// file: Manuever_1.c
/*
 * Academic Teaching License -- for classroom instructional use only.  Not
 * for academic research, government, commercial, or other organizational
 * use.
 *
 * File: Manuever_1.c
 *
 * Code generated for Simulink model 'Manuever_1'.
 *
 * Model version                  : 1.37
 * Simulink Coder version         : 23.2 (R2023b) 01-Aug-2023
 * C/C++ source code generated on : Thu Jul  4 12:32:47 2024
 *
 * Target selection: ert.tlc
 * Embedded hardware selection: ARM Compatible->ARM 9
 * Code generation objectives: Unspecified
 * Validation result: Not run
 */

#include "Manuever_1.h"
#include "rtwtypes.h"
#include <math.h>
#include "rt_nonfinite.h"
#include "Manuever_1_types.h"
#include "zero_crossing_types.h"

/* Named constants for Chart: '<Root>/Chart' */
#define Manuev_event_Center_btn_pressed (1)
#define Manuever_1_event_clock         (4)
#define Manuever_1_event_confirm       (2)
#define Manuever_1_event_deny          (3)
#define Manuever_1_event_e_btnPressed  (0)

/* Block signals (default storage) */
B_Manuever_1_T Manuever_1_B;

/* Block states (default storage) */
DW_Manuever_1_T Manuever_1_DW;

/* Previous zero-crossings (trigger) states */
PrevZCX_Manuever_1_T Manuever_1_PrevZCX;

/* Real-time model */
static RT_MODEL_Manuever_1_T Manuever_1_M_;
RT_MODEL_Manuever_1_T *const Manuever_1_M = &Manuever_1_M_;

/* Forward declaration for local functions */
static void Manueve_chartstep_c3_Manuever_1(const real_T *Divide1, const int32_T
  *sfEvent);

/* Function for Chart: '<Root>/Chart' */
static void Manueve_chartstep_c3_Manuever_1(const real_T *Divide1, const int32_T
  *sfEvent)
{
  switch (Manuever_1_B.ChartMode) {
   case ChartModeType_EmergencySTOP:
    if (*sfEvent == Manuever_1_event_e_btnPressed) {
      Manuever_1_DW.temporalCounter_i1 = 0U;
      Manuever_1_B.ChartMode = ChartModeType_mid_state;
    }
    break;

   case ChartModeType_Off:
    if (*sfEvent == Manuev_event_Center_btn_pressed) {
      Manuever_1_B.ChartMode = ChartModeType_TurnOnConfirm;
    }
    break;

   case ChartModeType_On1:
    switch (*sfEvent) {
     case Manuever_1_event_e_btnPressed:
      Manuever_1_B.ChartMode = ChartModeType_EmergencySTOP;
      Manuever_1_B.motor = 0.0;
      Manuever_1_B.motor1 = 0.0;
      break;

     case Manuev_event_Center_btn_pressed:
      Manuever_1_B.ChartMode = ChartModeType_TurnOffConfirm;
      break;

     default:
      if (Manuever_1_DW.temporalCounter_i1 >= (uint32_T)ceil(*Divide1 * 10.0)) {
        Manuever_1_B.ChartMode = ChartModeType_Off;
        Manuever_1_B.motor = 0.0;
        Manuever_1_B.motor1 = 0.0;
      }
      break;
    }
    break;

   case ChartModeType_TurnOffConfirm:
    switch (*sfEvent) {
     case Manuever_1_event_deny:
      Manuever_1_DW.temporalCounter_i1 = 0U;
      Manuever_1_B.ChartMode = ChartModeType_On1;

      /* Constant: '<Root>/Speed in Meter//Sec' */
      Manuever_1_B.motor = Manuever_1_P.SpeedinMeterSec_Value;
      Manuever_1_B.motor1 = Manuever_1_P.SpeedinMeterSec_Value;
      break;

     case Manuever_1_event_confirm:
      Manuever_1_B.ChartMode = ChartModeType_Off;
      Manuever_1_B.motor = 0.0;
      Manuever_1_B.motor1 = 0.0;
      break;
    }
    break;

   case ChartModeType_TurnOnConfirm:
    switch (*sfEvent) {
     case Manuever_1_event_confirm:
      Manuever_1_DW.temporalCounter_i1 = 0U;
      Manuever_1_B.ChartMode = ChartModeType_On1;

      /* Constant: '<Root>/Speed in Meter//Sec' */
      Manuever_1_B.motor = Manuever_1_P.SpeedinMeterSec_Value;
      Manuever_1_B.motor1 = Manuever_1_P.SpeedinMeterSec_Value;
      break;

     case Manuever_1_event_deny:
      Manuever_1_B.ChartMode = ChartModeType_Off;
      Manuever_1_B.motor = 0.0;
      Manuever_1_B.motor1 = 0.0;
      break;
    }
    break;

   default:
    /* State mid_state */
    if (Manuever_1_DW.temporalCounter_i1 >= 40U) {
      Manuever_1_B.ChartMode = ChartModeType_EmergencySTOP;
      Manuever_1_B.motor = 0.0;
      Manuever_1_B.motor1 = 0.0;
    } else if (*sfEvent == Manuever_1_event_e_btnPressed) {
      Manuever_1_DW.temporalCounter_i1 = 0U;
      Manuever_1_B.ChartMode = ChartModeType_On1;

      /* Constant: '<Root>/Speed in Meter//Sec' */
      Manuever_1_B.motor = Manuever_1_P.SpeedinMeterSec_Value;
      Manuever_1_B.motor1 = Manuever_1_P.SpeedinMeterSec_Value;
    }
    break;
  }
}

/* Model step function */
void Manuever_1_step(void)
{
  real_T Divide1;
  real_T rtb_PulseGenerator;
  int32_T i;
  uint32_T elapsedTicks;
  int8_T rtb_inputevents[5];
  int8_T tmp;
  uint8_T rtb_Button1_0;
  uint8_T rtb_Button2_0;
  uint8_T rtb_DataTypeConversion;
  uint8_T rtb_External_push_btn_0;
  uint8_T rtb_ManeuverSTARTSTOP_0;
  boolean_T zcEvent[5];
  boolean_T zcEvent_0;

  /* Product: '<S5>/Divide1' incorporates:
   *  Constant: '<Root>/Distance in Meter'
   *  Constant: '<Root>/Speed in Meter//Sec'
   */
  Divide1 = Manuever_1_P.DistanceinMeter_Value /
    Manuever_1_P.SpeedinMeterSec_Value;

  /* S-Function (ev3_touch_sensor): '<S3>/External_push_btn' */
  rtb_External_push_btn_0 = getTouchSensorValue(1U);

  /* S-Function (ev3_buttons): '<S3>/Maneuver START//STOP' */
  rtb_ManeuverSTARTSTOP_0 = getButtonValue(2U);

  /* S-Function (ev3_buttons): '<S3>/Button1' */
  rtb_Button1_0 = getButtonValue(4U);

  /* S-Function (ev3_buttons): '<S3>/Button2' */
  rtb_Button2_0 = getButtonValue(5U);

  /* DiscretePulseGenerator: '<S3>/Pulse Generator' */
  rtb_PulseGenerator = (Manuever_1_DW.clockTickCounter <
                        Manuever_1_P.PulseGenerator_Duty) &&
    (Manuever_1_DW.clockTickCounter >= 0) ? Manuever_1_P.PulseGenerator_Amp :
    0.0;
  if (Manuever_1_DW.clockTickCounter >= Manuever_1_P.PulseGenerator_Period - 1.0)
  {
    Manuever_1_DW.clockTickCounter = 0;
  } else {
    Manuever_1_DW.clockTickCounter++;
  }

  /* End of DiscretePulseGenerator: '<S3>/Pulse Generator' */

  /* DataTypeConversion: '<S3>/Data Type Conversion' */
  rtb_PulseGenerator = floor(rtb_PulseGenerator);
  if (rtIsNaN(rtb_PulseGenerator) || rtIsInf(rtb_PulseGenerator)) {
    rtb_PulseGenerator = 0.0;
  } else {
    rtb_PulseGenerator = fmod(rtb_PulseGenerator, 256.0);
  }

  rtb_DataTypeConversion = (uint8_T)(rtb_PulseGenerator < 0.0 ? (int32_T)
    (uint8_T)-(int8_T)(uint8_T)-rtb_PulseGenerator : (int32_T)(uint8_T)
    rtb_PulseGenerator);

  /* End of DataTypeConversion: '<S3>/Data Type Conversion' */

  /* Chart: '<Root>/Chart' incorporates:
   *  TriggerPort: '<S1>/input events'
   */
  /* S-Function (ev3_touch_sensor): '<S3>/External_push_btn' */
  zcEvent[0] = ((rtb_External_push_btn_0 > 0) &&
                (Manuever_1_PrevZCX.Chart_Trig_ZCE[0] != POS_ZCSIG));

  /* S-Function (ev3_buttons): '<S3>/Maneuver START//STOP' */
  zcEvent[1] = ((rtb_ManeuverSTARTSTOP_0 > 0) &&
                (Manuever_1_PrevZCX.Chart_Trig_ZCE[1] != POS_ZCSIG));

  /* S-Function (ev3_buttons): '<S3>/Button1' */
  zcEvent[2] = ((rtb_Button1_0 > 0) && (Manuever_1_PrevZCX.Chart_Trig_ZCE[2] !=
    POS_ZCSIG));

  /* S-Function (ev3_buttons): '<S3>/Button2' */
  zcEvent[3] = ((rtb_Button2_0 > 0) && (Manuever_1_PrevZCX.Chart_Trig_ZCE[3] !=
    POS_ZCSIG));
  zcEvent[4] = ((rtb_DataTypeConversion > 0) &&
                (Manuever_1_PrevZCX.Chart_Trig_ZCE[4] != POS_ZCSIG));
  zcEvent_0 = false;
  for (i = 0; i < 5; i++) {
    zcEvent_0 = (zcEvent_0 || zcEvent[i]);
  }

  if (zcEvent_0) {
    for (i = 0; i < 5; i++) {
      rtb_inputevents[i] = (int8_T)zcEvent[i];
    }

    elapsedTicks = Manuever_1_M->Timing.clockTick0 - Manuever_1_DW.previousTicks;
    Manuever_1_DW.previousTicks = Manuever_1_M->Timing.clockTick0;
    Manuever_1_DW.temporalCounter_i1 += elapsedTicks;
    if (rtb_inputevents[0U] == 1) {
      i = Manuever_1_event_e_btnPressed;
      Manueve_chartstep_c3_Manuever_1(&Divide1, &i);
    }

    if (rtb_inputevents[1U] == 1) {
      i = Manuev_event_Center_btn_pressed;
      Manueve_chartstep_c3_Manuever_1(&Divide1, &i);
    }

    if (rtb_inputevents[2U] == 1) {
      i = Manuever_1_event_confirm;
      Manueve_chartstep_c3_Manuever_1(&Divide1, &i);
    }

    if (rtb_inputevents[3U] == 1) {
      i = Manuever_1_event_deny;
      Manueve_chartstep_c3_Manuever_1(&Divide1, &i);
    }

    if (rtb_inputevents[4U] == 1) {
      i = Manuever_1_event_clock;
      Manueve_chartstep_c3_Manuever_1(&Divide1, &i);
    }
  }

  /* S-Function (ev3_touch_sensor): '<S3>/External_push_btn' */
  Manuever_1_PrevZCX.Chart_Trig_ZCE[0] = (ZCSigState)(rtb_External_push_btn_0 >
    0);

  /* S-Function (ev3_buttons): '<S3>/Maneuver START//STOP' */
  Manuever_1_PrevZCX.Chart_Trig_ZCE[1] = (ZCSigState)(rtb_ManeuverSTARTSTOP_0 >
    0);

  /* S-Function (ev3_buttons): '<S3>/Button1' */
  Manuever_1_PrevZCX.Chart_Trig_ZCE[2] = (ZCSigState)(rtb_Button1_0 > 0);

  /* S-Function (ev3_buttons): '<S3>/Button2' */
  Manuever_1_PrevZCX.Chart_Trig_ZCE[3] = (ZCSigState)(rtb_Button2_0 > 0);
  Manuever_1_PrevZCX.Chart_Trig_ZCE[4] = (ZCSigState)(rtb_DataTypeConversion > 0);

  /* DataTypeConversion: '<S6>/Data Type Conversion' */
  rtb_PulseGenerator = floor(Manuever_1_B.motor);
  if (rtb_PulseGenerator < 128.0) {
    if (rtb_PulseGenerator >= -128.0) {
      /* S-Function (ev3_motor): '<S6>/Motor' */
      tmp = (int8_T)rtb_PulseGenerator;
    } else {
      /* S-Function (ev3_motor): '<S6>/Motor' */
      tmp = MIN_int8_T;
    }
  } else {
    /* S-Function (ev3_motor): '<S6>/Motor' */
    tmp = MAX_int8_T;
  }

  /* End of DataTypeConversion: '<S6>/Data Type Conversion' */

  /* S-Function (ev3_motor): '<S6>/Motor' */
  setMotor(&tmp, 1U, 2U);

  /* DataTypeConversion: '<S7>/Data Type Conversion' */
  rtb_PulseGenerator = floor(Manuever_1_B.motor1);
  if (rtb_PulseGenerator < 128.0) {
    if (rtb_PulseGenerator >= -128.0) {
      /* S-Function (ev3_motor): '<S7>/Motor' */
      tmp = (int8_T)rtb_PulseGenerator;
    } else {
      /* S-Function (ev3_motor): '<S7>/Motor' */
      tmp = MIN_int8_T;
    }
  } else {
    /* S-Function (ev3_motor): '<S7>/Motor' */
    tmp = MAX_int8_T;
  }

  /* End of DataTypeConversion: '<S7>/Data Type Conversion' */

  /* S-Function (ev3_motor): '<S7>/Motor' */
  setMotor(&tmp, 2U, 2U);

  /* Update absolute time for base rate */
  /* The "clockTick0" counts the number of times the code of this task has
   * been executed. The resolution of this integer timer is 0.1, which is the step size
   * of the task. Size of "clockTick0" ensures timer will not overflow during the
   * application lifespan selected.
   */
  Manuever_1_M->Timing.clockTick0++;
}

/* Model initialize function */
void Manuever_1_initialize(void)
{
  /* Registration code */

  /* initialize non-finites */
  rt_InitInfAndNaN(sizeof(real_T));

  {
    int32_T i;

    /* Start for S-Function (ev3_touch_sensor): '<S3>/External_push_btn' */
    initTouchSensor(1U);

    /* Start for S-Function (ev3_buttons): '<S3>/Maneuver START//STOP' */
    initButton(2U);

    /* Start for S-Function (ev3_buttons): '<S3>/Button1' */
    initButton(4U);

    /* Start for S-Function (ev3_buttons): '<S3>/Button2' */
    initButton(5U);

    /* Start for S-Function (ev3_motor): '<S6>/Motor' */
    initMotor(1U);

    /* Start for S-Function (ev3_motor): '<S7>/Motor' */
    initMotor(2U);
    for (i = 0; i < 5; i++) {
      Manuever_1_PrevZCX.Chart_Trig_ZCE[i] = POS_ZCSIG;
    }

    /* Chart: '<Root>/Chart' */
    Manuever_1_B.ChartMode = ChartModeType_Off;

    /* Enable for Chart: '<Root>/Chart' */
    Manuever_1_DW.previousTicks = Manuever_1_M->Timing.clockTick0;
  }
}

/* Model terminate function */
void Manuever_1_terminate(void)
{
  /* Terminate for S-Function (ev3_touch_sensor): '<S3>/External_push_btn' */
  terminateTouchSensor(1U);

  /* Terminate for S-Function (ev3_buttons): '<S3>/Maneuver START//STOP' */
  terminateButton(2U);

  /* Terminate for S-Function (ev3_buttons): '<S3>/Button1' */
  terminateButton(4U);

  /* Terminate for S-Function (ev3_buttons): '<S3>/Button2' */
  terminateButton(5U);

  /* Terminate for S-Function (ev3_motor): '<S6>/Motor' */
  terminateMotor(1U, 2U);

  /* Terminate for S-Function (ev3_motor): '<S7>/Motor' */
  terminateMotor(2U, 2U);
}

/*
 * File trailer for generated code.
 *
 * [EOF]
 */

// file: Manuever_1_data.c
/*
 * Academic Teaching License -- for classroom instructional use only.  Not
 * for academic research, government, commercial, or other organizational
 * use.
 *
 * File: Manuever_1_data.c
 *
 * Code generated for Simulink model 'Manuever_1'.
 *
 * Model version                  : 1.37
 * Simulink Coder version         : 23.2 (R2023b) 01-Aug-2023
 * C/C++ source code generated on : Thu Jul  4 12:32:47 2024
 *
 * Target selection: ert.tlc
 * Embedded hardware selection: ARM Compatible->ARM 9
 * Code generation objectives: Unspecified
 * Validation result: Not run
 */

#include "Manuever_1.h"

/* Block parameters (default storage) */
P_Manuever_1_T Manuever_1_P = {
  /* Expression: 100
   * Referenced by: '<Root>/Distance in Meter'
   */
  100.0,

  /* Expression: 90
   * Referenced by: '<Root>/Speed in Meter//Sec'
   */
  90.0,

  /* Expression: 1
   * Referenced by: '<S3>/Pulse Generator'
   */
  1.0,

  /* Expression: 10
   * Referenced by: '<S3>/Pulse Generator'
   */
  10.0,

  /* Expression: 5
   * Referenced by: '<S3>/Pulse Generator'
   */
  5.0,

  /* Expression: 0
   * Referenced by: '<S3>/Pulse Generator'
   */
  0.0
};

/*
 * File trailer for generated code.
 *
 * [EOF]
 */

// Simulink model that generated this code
simulink model "Manuever_1"  (R2023b)
settings: Solver=FixedStepAuto  StartTime=0.0  StopTime=10  RelTol=1e-3  EnableMultiTasking=on
libraries: legoev3lib x7

== system Manuever_1 ==
  Chart : Stateflow chart  TreatAsAtomicUnit=on
  Distance Needed to Travel in Straight Line : Subsystem
  Distance in Meter : Constant  Value=100
  Mux : Mux  Inputs=5
  Speed in Meter/Sec : Constant  Value=90
  inputs : Subsystem
  outputs : Subsystem
  wires:
  Mux/1 -> Chart/Trigger
  inputs/1(Out1) -> Mux/1
  inputs/2(Out2) -> Mux/2
  inputs/3(Out3) -> Mux/3
  inputs/4(Out4) -> Mux/4
  inputs/5(Out5) -> Mux/5
  Chart/1(motor) -> outputs/1(In4)
  Chart/2(ChartMode) -> outputs/2(In5)
  Chart/3(motor1) -> outputs/3(motor1)
  Speed in Meter/Sec/1 -> Distance Needed to Travel in Straight Line/2(Speed_In)
  Distance Needed to Travel in Straight Line/1(Time_Out) -> Chart/1(Time_Out)
  Distance in Meter/1 -> Distance Needed to Travel in Straight Line/1(Distance_In)
  Distance Needed to Travel in Straight Line/2(Speed_Out) -> Chart/2(Speed_Out)

== system Manuever_1/Distance Needed to Travel in Straight Line ==
  Distance_In : Inport
  Speed_In : Inport  Port=2
  Distance Needed to Travel in Straight Line : Subsystem
  Time_Out : Outport
  Speed_Out : Outport  Port=2
  wires:
  Distance Needed to Travel in Straight Line/1(Time_Out) -> Time_Out/1
  Distance_In/1 -> Distance Needed to Travel in Straight Line/1(Distance_In)
  Speed_In/1 -> Distance Needed to Travel in Straight Line/2(Speed_In)
  Distance Needed to Travel in Straight Line/2(Speed-Out) -> Speed_Out/1

== system Manuever_1/inputs ==
  note: LEFT TO DENY COMMAND
  note: RIGHT TO CONFIRM COMAND
  Button1 : legoev3lib/Button  buttonType=Right  sampleTime=0.1
  Button2 : legoev3lib/Button  buttonType=Left  sampleTime=0.1
  Data Type Conversion : DataTypeConversion  OutDataTypeStr=uint8  SaturateOnIntegerOverflow=off  RndMeth=Floor
  External_push_btn : legoev3lib/Touch Sensor  portNumber=1  sampleTime=0.1
  Maneuver START/STOP : legoev3lib/Button  buttonType=Center  sampleTime=0.1
  Pulse Generator : DiscretePulseGenerator  Period=10  PulseWidth=5  SampleTime=0.1
  Out1 : Outport
  Out2 : Outport  Port=2
  Out3 : Outport  Port=3
  Out4 : Outport  Port=4
  Out5 : Outport  Port=5
  wires:
  Pulse Generator/1 -> Data Type Conversion/1
  Maneuver START/STOP/1 -> Out2/1
  Button2/1 -> Out4/1
  Button1/1 -> Out3/1
  Data Type Conversion/1 -> Out5/1
  External_push_btn/1 -> Out1/1

== system Manuever_1/outputs ==
  In4 : Inport
  In5 : Inport  Port=2
  motor1 : Inport  Port=3
  Display2 : legoev3lib/Display  Commented=on  slcdStr=Idle  slcdLine=1  slcdFormat=Decimal
  Motor : legoev3lib/Motor  sportNumber=A  sstopAction=Brake
  Motor1 : legoev3lib/Motor  sportNumber=B  sstopAction=Brake
  Scope : Scope
  wires:
  In4/1 -> Motor/1
  In5/1 -> Scope/1
  motor1/1 -> Motor1/1

== system Manuever_1/Distance Needed to Travel in Straight Line/Distance Needed to Travel in Straight Line ==
  Distance_In : Inport
  Speed_In : Inport  Port=2
  Divide1 : Product  Inputs=*/
  Time_Out : Outport
  Speed-Out : Outport  Port=2
  wires:
  Speed_In/1 -> Divide1/2, Speed-Out/1
  Distance_In/1 -> Divide1/1
  Divide1/1 -> Time_Out/1

== stateflow chart Manuever_1/Chart ==
  settings: executeAtInitialization=1
  state TurnOffConfirm
    entry:
  state Off
    entry:
    motor=0;
    motor1=0;
  state On1
    entry:
    motor =Speed_Out;
    motor1=Speed_Out;
  state TurnOnConfirm
  state EmergencySTOP
    entry:
    motor=0;
    motor1=0;
  state mid_state
  TurnOffConfirm -> (junction 129) [order 2] : confirm
  (junction 129) -> Off
  TurnOffConfirm -> On1 [order 1] : deny
  On1 -> TurnOffConfirm [order 2] : Center_btn_pressed
  (default) -> Off
  TurnOnConfirm -> Off [order 2] : deny
  TurnOnConfirm -> On1 [order 1] : confirm
  Off -> TurnOnConfirm : Center_btn_pressed
  (junction 143) -> Off
  On1 -> (junction 142) [order 3]
  (junction 113) -> On1
  On1 -> (junction 115) [order 1]
  (junction 115) -> EmergencySTOP : e_btnPressed
  EmergencySTOP -> (junction 128)
  (junction 120) -> EmergencySTOP
  mid_state -> (junction 113) [order 2] : e_btnPressed
  (junction 128) -> mid_state : e_btnPressed
  mid_state -> (junction 120) [order 1] : after(4,sec)
  (junction 142) -> (junction 143) : after(Time_Out,sec)
  data: motor output =0; ChartMode output Enum: ChartModeType; motor1 output; Time_Out input; Speed_Out input
  events: e_btnPressed input RISING_EDGE_EVENT; Center_btn_pressed input RISING_EDGE_EVENT; confirm input RISING_EDGE_EVENT; deny input RISING_EDGE_EVENT; clock input RISING_EDGE_EVENT
